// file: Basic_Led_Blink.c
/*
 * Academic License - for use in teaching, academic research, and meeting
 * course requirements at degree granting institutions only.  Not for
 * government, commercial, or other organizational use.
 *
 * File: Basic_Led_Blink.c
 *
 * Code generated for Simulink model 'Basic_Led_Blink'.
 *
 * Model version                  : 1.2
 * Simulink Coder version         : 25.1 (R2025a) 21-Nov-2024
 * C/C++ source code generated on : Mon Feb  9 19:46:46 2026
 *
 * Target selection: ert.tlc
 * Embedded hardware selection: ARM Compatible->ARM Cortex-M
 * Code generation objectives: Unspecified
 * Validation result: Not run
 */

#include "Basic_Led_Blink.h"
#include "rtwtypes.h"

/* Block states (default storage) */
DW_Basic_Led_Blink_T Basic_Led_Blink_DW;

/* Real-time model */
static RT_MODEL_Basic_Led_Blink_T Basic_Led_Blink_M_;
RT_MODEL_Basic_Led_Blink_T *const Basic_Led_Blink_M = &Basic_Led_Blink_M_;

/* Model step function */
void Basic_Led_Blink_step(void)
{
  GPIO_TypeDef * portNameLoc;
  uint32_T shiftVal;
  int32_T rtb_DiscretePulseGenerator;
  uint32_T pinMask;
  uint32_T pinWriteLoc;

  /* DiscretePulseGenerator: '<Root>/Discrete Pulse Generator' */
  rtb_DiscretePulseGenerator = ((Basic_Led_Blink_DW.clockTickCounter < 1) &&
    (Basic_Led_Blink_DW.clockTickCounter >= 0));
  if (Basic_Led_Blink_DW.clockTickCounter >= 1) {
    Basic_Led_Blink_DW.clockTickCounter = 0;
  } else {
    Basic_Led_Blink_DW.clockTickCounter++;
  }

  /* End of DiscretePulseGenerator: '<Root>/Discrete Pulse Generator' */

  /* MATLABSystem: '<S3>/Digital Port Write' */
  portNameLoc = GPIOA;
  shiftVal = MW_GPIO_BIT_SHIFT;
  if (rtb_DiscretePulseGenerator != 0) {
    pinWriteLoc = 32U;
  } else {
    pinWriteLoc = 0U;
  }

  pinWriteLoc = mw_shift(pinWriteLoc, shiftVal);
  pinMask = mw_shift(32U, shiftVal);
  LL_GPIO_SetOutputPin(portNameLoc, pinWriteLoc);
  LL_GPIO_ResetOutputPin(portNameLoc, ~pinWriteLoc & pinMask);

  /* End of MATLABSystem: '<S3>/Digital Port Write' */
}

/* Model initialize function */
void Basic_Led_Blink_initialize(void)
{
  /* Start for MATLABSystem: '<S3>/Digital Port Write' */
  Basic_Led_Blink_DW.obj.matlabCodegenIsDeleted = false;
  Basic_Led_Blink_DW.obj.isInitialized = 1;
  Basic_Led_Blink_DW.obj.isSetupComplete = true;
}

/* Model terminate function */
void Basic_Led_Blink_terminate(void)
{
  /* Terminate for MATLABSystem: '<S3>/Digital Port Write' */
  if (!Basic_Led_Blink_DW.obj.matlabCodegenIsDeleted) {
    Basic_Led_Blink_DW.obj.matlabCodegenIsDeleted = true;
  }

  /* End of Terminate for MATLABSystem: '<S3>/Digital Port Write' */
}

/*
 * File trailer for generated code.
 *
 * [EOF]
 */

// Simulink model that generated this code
simulink model "Basic_Led_Blink"  (R2025a)
settings: Solver=FixedStepAuto  StartTime=0.0  StopTime=10.0  RelTol=1e-3  EnableMultiTasking=on
libraries: stm32f4xxblockslib x1

== system Basic_Led_Blink ==
  note: Onboard LED Toggle
  Digital Port Write : stm32f4xxblockslib/Digital Port Write  PortName=GPIOA  PinNumber=[5]  ReadOperation=off  IOAsArray=on  EnableSimPort=off  hoistedMaskSrc=ECSoC/ECSimCodegen/Digital Port Write
  Discrete Pulse Generator : DiscretePulseGenerator  PulseType=Time based  PulseWidth=50
  wires:
  Discrete Pulse Generator/1 -> Digital Port Write/1
